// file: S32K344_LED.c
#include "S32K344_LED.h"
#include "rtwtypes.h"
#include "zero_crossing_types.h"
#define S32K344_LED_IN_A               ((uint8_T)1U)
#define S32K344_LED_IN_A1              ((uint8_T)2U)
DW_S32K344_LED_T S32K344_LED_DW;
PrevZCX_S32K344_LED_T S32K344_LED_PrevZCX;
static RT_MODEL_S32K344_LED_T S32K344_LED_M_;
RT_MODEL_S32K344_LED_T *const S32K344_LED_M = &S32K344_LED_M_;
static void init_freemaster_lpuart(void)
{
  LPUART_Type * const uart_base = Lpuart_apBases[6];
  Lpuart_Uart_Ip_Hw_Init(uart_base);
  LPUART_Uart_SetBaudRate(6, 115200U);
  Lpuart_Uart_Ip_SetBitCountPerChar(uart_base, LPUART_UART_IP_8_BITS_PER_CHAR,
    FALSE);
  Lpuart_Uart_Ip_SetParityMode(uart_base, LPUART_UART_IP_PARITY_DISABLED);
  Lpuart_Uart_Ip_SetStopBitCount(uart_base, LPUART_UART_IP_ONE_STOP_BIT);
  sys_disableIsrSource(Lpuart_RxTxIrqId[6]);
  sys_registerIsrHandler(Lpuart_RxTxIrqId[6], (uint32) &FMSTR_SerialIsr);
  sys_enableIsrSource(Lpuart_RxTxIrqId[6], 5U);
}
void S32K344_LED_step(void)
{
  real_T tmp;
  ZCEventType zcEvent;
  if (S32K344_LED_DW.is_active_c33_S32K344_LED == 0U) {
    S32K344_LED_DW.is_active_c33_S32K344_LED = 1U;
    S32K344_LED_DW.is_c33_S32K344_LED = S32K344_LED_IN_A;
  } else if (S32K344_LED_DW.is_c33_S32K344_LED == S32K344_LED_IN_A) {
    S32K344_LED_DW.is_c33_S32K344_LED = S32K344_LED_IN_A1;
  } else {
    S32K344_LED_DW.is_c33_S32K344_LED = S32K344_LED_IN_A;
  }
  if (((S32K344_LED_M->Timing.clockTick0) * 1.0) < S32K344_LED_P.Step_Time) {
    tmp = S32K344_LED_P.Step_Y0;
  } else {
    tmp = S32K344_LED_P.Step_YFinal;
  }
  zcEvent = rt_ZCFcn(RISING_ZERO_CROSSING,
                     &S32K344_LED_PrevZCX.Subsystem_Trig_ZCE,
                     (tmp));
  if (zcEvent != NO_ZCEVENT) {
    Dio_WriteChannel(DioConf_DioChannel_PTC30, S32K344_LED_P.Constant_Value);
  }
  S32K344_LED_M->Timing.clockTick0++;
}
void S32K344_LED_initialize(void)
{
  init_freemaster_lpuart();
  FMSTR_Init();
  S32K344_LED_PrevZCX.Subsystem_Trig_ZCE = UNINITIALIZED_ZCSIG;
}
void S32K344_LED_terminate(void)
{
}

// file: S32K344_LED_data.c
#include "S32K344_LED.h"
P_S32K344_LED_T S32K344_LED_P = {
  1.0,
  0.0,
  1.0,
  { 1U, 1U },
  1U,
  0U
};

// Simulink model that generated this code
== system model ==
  Subsystem#1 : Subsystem  <- Trigger: FunctionCallGenerator#1
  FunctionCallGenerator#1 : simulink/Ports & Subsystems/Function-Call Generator
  FreeMASTERConfig#1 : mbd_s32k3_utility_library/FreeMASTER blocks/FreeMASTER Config
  DataStoreMemory#1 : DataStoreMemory
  Subsystem#2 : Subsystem  <- Trigger: FunctionCallGenerator#2
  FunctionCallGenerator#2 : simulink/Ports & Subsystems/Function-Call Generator
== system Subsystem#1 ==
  TriggerPort#1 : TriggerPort  TriggerType=function-call
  DataStoreWrite#1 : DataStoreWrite  Indices=1  <- 1: DataTypeConversion#1
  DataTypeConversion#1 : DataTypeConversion  <- 1: Stateflowchart#1
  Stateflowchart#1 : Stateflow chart
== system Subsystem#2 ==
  TriggerPort#2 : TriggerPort  TriggerType=function-call
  Uart : mbd_s32k3_cdd_library/Uart  <- 1: Dio
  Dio : mbd_s32k3_io_library/Dio
== stateflow chart Stateflowchart#1 ==
  state A
  state A1
  (default) -> A
  A -> A1
  A1 -> A
  data: A output boolean [0..1]
